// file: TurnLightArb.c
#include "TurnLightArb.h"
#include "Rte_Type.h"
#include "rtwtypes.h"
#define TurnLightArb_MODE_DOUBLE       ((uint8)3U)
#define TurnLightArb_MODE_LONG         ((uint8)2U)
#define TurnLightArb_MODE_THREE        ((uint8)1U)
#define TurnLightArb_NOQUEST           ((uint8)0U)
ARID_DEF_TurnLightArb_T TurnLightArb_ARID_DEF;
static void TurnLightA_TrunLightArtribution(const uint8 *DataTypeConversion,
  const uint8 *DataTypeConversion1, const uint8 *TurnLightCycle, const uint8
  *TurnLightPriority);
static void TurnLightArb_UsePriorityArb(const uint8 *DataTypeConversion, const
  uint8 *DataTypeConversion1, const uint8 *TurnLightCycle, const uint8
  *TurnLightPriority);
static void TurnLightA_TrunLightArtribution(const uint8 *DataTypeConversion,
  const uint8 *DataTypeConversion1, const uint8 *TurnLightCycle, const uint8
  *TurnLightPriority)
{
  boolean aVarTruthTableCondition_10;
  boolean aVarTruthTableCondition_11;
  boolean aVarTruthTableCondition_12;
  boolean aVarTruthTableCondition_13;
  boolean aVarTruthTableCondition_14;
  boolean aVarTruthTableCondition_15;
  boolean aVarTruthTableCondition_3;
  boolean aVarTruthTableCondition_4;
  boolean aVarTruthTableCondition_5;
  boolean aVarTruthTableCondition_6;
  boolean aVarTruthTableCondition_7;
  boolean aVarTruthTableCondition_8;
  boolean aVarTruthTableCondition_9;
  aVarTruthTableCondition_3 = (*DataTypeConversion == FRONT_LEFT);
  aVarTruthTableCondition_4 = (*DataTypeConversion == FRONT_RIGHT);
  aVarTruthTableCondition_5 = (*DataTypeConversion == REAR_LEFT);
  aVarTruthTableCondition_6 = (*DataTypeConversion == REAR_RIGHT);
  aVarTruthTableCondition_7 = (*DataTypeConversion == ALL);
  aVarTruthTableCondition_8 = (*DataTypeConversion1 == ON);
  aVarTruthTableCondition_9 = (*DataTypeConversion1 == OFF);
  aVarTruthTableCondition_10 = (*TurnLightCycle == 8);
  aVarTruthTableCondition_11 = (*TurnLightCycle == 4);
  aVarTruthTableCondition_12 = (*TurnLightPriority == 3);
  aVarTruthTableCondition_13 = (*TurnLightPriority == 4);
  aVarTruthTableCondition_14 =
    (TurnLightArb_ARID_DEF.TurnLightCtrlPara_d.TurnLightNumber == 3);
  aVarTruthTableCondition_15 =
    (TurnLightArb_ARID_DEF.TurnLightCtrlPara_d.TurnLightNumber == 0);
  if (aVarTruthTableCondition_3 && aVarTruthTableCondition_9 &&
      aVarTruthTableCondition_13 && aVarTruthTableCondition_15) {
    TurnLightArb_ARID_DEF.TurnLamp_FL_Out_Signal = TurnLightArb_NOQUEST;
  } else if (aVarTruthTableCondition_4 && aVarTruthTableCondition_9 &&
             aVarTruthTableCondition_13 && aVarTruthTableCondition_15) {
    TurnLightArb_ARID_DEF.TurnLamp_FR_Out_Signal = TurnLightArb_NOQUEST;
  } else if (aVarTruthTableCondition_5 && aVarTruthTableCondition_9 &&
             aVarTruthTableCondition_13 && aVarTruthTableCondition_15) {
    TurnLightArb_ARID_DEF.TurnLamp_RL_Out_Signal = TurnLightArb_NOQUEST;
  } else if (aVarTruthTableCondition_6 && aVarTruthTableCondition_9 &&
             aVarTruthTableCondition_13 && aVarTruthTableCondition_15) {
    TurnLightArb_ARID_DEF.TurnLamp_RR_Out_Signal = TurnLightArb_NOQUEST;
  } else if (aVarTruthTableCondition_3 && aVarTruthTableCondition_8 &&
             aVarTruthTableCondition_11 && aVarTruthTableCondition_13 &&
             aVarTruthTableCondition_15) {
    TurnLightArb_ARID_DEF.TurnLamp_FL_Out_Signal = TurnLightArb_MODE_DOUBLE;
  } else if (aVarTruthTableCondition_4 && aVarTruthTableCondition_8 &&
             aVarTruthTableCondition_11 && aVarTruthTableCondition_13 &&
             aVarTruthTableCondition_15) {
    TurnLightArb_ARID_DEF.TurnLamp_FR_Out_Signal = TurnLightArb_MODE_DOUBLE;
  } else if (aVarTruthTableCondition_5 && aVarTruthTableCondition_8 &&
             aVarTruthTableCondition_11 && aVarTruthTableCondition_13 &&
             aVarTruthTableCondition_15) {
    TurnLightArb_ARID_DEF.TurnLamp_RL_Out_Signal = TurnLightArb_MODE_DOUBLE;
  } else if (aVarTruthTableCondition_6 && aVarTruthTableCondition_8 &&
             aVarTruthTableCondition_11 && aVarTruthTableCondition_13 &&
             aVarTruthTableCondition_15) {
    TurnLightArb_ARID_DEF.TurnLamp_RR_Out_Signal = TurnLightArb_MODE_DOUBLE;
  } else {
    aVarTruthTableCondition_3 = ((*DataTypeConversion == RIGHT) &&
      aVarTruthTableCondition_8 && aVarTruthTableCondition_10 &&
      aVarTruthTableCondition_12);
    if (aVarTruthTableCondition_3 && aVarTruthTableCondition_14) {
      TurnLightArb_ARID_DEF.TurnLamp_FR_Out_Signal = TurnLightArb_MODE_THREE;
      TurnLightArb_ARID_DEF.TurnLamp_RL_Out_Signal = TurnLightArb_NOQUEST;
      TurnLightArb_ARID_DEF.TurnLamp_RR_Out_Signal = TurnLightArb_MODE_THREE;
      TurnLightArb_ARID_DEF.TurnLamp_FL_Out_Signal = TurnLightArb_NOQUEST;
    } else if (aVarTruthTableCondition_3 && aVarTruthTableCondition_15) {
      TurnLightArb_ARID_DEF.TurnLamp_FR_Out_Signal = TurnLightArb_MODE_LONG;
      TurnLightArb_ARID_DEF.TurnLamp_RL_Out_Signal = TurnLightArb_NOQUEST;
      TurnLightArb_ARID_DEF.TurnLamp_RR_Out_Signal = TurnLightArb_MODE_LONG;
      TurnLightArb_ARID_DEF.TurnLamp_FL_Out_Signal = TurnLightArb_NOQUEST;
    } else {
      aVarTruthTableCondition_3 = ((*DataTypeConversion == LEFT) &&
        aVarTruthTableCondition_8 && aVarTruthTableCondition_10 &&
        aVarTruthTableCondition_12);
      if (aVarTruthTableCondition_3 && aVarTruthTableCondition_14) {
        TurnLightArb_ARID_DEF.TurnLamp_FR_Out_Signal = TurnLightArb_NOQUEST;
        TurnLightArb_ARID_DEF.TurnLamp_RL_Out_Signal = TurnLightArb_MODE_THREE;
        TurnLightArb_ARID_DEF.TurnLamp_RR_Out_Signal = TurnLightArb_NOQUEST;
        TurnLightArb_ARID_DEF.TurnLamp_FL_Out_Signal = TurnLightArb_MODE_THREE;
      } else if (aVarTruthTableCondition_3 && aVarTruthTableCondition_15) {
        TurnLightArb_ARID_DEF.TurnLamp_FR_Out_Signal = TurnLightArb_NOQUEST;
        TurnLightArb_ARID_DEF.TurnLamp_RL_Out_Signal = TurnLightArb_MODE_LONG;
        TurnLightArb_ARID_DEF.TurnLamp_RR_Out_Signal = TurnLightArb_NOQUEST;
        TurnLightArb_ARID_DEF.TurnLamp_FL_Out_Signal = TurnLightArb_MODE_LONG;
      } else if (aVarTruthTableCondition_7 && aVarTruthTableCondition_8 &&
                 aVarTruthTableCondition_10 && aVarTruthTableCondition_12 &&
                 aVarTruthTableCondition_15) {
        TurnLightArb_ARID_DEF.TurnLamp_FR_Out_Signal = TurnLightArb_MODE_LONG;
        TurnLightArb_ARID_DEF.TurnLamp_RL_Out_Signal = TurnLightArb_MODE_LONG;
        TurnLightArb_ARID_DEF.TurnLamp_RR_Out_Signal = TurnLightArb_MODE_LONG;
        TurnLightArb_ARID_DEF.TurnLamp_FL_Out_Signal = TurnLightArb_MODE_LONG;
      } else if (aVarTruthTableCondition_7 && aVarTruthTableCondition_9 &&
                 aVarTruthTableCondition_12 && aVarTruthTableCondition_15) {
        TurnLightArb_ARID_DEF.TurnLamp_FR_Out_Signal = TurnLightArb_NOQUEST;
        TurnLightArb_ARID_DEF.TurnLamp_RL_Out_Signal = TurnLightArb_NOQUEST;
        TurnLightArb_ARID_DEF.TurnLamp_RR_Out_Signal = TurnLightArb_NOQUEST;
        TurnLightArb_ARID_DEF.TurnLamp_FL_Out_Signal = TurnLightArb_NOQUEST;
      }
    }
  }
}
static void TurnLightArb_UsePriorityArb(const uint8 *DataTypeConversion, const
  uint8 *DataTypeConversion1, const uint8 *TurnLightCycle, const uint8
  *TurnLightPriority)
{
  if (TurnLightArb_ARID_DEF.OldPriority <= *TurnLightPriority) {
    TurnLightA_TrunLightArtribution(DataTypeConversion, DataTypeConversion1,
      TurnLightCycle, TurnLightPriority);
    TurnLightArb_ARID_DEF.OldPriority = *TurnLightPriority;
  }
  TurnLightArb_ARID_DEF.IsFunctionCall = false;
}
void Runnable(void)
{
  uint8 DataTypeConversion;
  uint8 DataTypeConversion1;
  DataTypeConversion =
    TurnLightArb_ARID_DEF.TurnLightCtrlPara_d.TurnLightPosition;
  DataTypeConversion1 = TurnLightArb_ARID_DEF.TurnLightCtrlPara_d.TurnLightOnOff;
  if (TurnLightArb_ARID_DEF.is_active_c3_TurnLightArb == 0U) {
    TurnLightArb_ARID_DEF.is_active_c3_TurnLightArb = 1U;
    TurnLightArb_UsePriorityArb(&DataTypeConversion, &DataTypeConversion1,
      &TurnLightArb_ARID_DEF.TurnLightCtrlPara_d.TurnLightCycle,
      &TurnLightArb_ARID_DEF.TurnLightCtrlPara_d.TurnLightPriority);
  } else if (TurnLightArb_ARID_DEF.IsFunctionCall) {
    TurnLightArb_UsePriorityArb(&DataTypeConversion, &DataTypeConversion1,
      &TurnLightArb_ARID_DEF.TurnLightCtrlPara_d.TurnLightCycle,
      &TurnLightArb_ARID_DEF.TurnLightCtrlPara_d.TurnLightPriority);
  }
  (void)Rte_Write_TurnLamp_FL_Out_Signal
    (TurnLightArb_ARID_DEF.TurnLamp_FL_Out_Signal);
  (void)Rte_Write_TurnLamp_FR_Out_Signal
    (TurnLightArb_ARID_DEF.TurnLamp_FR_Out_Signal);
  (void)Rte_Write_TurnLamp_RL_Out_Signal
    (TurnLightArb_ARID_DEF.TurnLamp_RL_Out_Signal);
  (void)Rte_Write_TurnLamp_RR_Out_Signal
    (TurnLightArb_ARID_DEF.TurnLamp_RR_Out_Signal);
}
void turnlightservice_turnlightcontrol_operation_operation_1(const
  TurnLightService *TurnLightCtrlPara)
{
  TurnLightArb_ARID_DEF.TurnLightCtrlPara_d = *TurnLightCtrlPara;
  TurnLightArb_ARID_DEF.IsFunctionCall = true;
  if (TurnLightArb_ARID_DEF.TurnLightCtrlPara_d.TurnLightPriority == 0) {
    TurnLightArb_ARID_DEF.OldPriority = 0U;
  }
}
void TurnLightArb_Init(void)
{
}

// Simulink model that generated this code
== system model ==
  Runnable : Inport
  TurnLamp_FL_Out_Signal : Outport  <- 1: Subsystem#1
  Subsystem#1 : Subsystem  <- Trigger: Runnable
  TurnLamp_FR_Out_Signal : Outport  <- 1: Subsystem#1/2
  TurnLamp_RL_Out_Signal : Outport  <- 1: Subsystem#1/3
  TurnLamp_RR_Out_Signal : Outport  <- 1: Subsystem#1/4
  DataStoreMemory#1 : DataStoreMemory  DataStoreName=TurnLightCtrlPara
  Subsystem#2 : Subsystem
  DataStoreMemory#2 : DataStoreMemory  DataStoreName=IsFunctionCall
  DataStoreMemory#3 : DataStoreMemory  DataStoreName=OldPriority
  EventListener#1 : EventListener
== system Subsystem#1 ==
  TriggerPort#1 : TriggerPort  TriggerType=function-call
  Outport#1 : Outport  <- 1: Stateflowchart#1/4
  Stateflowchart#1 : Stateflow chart  <- 1: BusSelector#1/4, 2: BusSelector#1/3, 3: BusSelector#1/7, 4: DataTypeConversion1, 5: DataTypeConversion, 6: BusSelector#1/6, 7: BusSelector#1/5
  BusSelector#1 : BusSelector  <- 1: DataStoreRead#1
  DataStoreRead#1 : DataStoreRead  DataStoreName=TurnLightCtrlPara  Indices=1
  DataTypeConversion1 : DataTypeConversion  <- 1: BusSelector#1/2
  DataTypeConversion : DataTypeConversion  <- 1: BusSelector#1
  Outport#2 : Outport  <- 1: Stateflowchart#1/3
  Outport#3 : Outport  <- 1: Stateflowchart#1/2
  Outport#4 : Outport  <- 1: Stateflowchart#1
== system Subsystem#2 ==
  TriggerPort#2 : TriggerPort  TriggerType=function-call  FunctionName=TurnLightService_TurnLightControl_Operation_Operation
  DataStoreWrite#1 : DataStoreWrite  DataStoreName=TurnLightCtrlPara  Indices=1  <- 1: TurnLightCtrlPara
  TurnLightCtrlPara : ArgIn
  DataStoreWrite#2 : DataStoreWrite  DataStoreName=IsFunctionCall  Indices=1  <- 1: Constant#1
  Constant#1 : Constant
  Subsystem#3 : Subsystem  <- Action: If#1
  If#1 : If  IfExpression=u1 == 0  <- 1: BusSelector#2
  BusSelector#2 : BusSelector  <- 1: TurnLightCtrlPara
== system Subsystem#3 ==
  ActionPort#1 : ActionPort
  DataStoreWrite#3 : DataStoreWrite  DataStoreName=OldPriority  Indices=1  <- 1: Constant#2
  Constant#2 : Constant  Value=0
== stateflow chart Stateflowchart#1 ==
  state IDLE_
    en:
    UsePriorityArb();
  state TrunLightArtribution [function]
    (default) -> (junction 448)
    (junction 448) -> (junction 450) : { aVarTruthTableCondition_1 = (TurnLightPosition==ComplexTurnLightPosition.RIGHT); }
    (junction 450) -> (junction 452) : { aVarTruthTableCondition_2 = (TurnLightPosition==ComplexTurnLightPosition.LEFT); }
    (junction 452) -> (junction 454) : { aVarTruthTableCondition_3 = (TurnLightPosition==ComplexTurnLightPosition.FRONT_LEFT); }
    (junction 454) -> (junction 456) : { aVarTruthTableCondition_4 = (TurnLightPosition==ComplexTurnLightPosition.FRONT_RIGHT); }
    (junction 456) -> (junction 458) : { aVarTruthTableCondition_5 = (TurnLightPosition==ComplexTurnLightPosition.REAR_LEFT); }
    (junction 458) -> (junction 460) : { aVarTruthTableCondition_6 = (TurnLightPosition==ComplexTurnLightPosition.REAR_RIGHT); }
    (junction 460) -> (junction 462) : { aVarTruthTableCondition_7 = (TurnLightPosition==ComplexTurnLightPosition.ALL); }
    (junction 462) -> (junction 464) : { aVarTruthTableCondition_8 = (TurnLightOnOff==ComplexTurnLightOnOff.ON); }
    (junction 464) -> (junction 466) : { aVarTruthTableCondition_9 = (TurnLightOnOff==ComplexTurnLightOnOff.OFF); }
    (junction 466) -> (junction 468) : { aVarTruthTableCondition_10 = (TurnLightCycle==8); }
    (junction 468) -> (junction 470) : { aVarTruthTableCondition_11 = (TurnLightCycle==4); }
    (junction 470) -> (junction 472) : { aVarTruthTableCondition_12 = (TurnLightPriority==3); }
    (junction 472) -> (junction 474) : { aVarTruthTableCondition_13 = (TurnLightPriority==4); }
    (junction 474) -> (junction 476) : { aVarTruthTableCondition_14 = (TurnLightNum==3); }
    (junction 476) -> (junction 478) : { aVarTruthTableCondition_15 = (TurnLightNum==0); }
    (junction 478) -> (junction 480) [order 1] : [aVarTruthTableCondition_3 && aVarTruthTableCondition_9 && aVarTruthTableCondition_13 && aVarTruthTableCondition_15]
    (junction 480) -> (junction 482) : {
        | /* 'FL_OFF': */
        | TurnLamp_FL_Out_Signal=NOQUEST;
        | }
    (junction 478) -> (junction 484) [order 2]
    (junction 484) -> (junction 486) [order 1] : [aVarTruthTableCondition_4 && aVarTruthTableCondition_9 && aVarTruthTableCondition_13 && aVarTruthTableCondition_15]
    (junction 486) -> (junction 488) : {
        | /* 'FR_OFF': */
        | TurnLamp_FR_Out_Signal=NOQUEST;
        | }
    (junction 484) -> (junction 490) [order 2]
    (junction 490) -> (junction 492) [order 1] : [aVarTruthTableCondition_5 && aVarTruthTableCondition_9 && aVarTruthTableCondition_13 && aVarTruthTableCondition_15]
    (junction 492) -> (junction 494) : {
        | /* 'RL_OFF': */
        | TurnLamp_RL_Out_Signal=NOQUEST;
        | }
    (junction 490) -> (junction 496) [order 2]
    (junction 496) -> (junction 498) [order 1] : [aVarTruthTableCondition_6 && aVarTruthTableCondition_9 && aVarTruthTableCondition_13 && aVarTruthTableCondition_15]
    (junction 498) -> (junction 500) : {
        | /* 'RR_OFF': */
        | TurnLamp_RR_Out_Signal=NOQUEST;
        | }
    (junction 496) -> (junction 502) [order 2]
    (junction 502) -> (junction 504) [order 1] : [aVarTruthTableCondition_3 && aVarTruthTableCondition_8 && aVarTruthTableCondition_11 && aVarTruthTableCondition_13 && aVarTruthTableCondition_15]
    (junction 504) -> (junction 506) : {
        | /* 'FL_DOUBLE': */
        | TurnLamp_FL_Out_Signal=MODE_DOUBLE;
        | }
    (junction 502) -> (junction 508) [order 2]
    (junction 508) -> (junction 510) [order 1] : [aVarTruthTableCondition_4 && aVarTruthTableCondition_8 && aVarTruthTableCondition_11 && aVarTruthTableCondition_13 && aVarTruthTableCondition_15]
    (junction 510) -> (junction 512) : {
        | /* 'FR_DOUBLE': */
        | TurnLamp_FR_Out_Signal=MODE_DOUBLE;
        | }
    (junction 508) -> (junction 514) [order 2]
    (junction 514) -> (junction 516) [order 1] : [aVarTruthTableCondition_5 && aVarTruthTableCondition_8 && aVarTruthTableCondition_11 && aVarTruthTableCondition_13 && aVarTruthTableCondition_15]
    (junction 516) -> (junction 518) : {
        | /* 'RL_DOUBLE': */
        | TurnLamp_RL_Out_Signal=MODE_DOUBLE;
        | }
    (junction 514) -> (junction 520) [order 2]
    (junction 520) -> (junction 522) [order 1] : [aVarTruthTableCondition_6 && aVarTruthTableCondition_8 && aVarTruthTableCondition_11 && aVarTruthTableCondition_13 && aVarTruthTableCondition_15]
    (junction 522) -> (junction 524) : {
        | /* 'RR_DOUBLE': */
        | TurnLamp_RR_Out_Signal=MODE_DOUBLE;
        | }
    (junction 520) -> (junction 526) [order 2]
    (junction 526) -> (junction 528) [order 1] : [aVarTruthTableCondition_1 && aVarTruthTableCondition_8 && aVarTruthTableCondition_10 && aVarTruthTableCondition_12 && aVarTruthTableCondition_14]
    (junction 528) -> (junction 530) : {
        | /* 'TurnLight_RightShort': */
        | TurnLamp_FR_Out_Signal=MODE_THREE;
        | TurnLamp_RL_Out_Signal=NOQUEST;
        | TurnLamp_RR_Out_Signal=MODE_THREE;
        | TurnLamp_FL_Out_Signal=NOQUEST;
        | }
    (junction 526) -> (junction 532) [order 2]
    (junction 532) -> (junction 534) [order 1] : [aVarTruthTableCondition_1 && aVarTruthTableCondition_8 && aVarTruthTableCondition_10 && aVarTruthTableCondition_12 && aVarTruthTableCondition_15]
    (junction 534) -> (junction 536) : {
        | /* 'TurnLight_RightLong': */
        | TurnLamp_FR_Out_Signal=MODE_LONG;
        | TurnLamp_RL_Out_Signal=NOQUEST;
        | TurnLamp_RR_Out_Signal=MODE_LONG;
        | TurnLamp_FL_Out_Signal=NOQUEST;
        | }
    (junction 532) -> (junction 538) [order 2]
    (junction 538) -> (junction 540) [order 1] : [aVarTruthTableCondition_2 && aVarTruthTableCondition_8 && aVarTruthTableCondition_10 && aVarTruthTableCondition_12 && aVarTruthTableCondition_14]
    (junction 540) -> (junction 542) : {
        | /* 'TurnLight_LeftShort': */
        | TurnLamp_FR_Out_Signal=NOQUEST;
        | TurnLamp_RL_Out_Signal=MODE_THREE;
        | TurnLamp_RR_Out_Signal=NOQUEST;
        | TurnLamp_FL_Out_Signal=MODE_THREE;
        | }
    (junction 538) -> (junction 544) [order 2]
    (junction 544) -> (junction 546) [order 1] : [aVarTruthTableCondition_2 && aVarTruthTableCondition_8 && aVarTruthTableCondition_10 && aVarTruthTableCondition_12 && aVarTruthTableCondition_15]
    (junction 546) -> (junction 548) : {
        | /* 'TurnLight_LeftLong': */
        | TurnLamp_FR_Out_Signal=NOQUEST;
        | TurnLamp_RL_Out_Signal=MODE_LONG;
        | TurnLamp_RR_Out_Signal=NOQUEST;
        | TurnLamp_FL_Out_Signal=MODE_LONG;
        | }
    (junction 544) -> (junction 550) [order 2]
    (junction 550) -> (junction 552) [order 1] : [aVarTruthTableCondition_7 && aVarTruthTableCondition_8 && aVarTruthTableCondition_10 && aVarTruthTableCondition_12 && aVarTruthTableCondition_15]
    (junction 552) -> (junction 554) : {
        | /* 'TurnLight_ALLON': */
        | TurnLamp_FR_Out_Signal=MODE_LONG;
        | TurnLamp_RL_Out_Signal=MODE_LONG;
        | TurnLamp_RR_Out_Signal=MODE_LONG;
        | TurnLamp_FL_Out_Signal=MODE_LONG;
        | }
    (junction 550) -> (junction 556) [order 2]
    (junction 556) -> (junction 558) : [aVarTruthTableCondition_7 && aVarTruthTableCondition_9 && aVarTruthTableCondition_12 && aVarTruthTableCondition_15]
    (junction 558) -> (junction 560) : {
        | /* 'TurnLight_ALLOFF': */
        | TurnLamp_FR_Out_Signal=NOQUEST;
        | TurnLamp_RL_Out_Signal=NOQUEST;
        | TurnLamp_RR_Out_Signal=NOQUEST;
        | TurnLamp_FL_Out_Signal=NOQUEST;
        | }
  state UsePriorityArb [function]
    (default) -> (junction 33)
    (junction 33) -> (junction 34) [order 1] : [OldPriority<=TurnLightPriority]
    (junction 33) -> (junction 35) [order 2]
    (junction 34) -> (junction 36) : {TrunLightArtribution();
        | OldPriority=TurnLightPriority;}
    (junction 36) -> (junction 35)
    (junction 35) -> (junction 37) : {IsFunctionCall=0;}
  (default) -> IDLE_
  IDLE_ -> IDLE_ : [IsFunctionCall==1]
  data: aVarTruthTableCondition_1 temporary boolean =0; aVarTruthTableCondition_2 temporary boolean =0; aVarTruthTableCondition_3 temporary boolean =0; aVarTruthTableCondition_4 temporary boolean =0; aVarTruthTableCondition_5 temporary boolean =0; aVarTruthTableCondition_6 temporary boolean =0; aVarTruthTableCondition_7 temporary boolean =0; aVarTruthTableCondition_8 temporary boolean =0; aVarTruthTableCondition_9 temporary boolean =0; aVarTruthTableCondition_10 temporary boolean =0; aVarTruthTableCondition_11 temporary boolean =0; aVarTruthTableCondition_12 temporary boolean =0; aVarTruthTableCondition_13 temporary boolean =0; aVarTruthTableCondition_14 temporary boolean =0; aVarTruthTableCondition_15 temporary boolean =0; TurnLightCycle input uint8; TurnLightDutyCycle input uint8; TurnLightNum input uint8; TurnLightOnOff input uint8; TurnLightPosition input uint8; TurnLightPriority input uint8; TurnLightTimes input uint8; TurnLamp_RR_Out_Signal output uint8; TurnLamp_RL_Out_Signal output uint8; TurnLamp_FR_Out_Signal output uint8; TurnLamp_FL_Out_Signal output uint8; IsFunctionCall data_store_memory; OldPriority data_store_memory; MODE_DOUBLE constant uint8 =3; MODE_LONG constant uint8 =2; MODE_THREE constant uint8 =1; NOQUEST constant uint8 =0
